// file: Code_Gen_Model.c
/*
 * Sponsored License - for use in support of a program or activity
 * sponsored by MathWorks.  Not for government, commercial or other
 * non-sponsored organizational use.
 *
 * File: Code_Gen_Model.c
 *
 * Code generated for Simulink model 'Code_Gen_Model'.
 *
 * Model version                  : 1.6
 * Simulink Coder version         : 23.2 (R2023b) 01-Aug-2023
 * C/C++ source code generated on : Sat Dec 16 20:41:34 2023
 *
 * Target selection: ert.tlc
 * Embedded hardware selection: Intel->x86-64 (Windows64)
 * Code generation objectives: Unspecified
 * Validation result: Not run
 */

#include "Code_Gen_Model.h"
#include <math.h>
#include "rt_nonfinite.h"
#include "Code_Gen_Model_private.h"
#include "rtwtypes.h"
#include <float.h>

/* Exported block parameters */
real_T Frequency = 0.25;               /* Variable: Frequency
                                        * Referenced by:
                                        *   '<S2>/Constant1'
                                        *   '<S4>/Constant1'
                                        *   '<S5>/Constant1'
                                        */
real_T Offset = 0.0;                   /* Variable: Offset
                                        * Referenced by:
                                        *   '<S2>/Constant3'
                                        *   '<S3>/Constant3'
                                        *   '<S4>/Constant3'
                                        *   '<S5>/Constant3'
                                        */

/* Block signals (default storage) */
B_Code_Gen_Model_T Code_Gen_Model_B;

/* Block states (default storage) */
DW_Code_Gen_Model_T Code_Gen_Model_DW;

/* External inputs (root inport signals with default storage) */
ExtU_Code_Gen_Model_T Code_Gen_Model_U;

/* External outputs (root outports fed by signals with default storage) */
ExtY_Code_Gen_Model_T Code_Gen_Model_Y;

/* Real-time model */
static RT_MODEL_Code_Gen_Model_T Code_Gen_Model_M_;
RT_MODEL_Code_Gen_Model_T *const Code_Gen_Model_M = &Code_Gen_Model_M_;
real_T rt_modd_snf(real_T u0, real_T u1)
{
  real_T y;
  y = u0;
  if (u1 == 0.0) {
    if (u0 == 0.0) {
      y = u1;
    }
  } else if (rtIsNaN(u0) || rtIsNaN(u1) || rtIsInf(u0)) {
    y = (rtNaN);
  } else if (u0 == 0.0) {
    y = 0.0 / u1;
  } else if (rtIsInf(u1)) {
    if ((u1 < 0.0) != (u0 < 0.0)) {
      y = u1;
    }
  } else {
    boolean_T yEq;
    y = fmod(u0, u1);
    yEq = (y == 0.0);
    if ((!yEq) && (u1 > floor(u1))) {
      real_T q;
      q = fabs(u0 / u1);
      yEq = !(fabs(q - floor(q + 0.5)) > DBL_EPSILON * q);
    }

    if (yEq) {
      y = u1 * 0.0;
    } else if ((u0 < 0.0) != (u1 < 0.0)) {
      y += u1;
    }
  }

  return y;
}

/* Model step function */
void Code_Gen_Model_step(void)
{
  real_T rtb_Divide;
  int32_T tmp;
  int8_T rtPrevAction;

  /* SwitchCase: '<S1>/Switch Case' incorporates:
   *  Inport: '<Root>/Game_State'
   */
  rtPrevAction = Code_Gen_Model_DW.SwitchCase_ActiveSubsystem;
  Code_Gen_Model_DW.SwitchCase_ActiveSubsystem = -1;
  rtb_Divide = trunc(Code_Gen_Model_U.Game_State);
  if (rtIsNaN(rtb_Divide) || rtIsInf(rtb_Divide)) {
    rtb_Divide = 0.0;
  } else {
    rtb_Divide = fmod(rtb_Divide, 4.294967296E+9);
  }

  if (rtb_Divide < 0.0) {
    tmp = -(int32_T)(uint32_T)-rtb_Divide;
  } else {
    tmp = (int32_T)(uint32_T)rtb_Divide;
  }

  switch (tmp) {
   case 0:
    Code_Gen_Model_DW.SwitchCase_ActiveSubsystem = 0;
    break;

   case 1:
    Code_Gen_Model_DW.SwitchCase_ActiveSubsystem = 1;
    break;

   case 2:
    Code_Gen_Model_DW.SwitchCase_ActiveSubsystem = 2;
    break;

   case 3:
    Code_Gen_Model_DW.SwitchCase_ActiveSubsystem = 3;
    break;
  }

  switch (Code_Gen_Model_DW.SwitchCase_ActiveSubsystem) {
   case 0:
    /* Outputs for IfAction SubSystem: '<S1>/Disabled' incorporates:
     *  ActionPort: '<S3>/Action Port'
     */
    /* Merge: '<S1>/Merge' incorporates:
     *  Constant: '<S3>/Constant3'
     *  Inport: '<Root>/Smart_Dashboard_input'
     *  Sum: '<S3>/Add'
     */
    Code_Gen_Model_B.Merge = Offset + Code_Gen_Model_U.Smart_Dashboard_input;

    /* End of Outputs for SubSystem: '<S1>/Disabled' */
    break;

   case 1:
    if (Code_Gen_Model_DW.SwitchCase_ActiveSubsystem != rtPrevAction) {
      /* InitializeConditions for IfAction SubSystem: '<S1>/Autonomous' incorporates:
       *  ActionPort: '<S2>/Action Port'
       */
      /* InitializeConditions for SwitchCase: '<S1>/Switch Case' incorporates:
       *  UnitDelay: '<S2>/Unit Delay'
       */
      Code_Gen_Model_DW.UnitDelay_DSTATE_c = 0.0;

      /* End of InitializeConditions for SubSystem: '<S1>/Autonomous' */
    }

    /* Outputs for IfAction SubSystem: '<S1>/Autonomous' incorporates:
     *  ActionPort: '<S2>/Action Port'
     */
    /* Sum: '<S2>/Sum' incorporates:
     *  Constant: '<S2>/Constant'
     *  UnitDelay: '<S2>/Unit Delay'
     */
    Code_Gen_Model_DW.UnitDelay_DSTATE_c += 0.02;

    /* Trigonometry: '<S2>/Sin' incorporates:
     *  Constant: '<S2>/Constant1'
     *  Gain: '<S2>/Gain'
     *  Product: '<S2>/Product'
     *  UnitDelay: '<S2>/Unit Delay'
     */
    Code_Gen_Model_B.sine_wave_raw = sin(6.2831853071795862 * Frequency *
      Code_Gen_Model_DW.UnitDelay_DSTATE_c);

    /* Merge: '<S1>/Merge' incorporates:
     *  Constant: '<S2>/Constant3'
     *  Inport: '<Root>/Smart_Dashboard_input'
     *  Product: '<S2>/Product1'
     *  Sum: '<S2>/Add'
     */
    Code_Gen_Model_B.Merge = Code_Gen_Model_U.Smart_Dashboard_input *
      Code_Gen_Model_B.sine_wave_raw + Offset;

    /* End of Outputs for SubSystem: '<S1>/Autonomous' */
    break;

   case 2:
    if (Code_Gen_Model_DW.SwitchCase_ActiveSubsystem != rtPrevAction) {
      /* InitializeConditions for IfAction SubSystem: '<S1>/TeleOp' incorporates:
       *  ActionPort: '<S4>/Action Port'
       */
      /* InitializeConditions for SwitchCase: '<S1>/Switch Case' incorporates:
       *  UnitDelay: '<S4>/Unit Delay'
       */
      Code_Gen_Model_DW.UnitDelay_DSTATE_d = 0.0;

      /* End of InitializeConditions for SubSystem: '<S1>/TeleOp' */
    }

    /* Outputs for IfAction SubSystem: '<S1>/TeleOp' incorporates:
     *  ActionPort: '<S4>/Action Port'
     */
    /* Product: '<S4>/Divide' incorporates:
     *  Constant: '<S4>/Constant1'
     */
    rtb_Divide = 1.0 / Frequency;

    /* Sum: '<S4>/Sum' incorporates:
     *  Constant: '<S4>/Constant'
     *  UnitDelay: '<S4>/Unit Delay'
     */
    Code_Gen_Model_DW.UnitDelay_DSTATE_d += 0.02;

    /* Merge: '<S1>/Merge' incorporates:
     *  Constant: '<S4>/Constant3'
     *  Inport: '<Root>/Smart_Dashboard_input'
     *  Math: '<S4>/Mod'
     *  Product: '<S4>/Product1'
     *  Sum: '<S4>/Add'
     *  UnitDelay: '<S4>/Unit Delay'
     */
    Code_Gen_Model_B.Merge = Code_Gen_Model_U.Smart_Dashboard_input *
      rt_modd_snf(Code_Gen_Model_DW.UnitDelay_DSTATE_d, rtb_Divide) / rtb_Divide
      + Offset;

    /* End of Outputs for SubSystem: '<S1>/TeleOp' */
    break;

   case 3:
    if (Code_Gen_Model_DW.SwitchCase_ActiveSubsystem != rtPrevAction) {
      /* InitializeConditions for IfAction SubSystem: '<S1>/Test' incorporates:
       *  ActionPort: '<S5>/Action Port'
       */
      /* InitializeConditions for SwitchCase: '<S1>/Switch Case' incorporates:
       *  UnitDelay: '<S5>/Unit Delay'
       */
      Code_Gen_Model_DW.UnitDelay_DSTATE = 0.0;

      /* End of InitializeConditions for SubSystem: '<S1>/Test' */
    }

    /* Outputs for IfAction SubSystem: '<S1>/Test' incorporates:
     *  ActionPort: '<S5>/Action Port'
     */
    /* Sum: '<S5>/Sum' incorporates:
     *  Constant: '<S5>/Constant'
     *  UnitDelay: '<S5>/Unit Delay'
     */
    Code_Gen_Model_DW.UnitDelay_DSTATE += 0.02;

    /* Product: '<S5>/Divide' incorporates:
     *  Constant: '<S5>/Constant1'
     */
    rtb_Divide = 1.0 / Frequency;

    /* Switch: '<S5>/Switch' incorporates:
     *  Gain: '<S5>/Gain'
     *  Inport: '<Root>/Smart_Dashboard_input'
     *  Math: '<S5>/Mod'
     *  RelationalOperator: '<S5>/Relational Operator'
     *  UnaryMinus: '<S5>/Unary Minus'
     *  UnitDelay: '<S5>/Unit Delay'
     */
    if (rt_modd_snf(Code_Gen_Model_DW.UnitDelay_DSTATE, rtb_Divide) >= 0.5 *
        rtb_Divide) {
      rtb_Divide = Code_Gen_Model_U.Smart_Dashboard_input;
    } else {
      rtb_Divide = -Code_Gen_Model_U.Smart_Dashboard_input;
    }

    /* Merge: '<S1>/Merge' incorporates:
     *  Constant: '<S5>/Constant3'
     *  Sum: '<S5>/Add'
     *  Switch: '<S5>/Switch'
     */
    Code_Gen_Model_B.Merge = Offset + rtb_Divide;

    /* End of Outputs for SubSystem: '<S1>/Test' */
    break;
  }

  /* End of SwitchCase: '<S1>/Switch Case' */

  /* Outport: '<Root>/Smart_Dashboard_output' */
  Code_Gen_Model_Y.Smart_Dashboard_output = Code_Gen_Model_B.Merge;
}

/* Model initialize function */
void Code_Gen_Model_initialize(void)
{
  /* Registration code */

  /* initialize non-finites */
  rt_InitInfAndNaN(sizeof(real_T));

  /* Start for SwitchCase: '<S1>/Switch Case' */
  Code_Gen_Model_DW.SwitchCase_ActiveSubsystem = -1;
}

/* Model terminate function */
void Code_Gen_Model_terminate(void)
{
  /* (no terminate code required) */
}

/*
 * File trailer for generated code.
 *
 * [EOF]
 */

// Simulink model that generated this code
simulink model "Code_Gen_Model"  (R2023b)
settings: Solver=FixedStepDiscrete  StartTime=0.0  StopTime=inf  FixedStep=t_sample  RelTol=1e-3

== system Code_Gen_Model ==
  Game_State : Inport
  Smart_Dashboard_input : Inport  Port=2
  Robot Subsystem : Subsystem  ReferencedSubsystem=Robot_sub
  Smart_Dashboard_output : Outport
  wires:
  Game_State/1 -> Robot Subsystem/1
  Smart_Dashboard_input/1 -> Robot Subsystem/2
  Robot Subsystem/1 -> Smart_Dashboard_output/1
